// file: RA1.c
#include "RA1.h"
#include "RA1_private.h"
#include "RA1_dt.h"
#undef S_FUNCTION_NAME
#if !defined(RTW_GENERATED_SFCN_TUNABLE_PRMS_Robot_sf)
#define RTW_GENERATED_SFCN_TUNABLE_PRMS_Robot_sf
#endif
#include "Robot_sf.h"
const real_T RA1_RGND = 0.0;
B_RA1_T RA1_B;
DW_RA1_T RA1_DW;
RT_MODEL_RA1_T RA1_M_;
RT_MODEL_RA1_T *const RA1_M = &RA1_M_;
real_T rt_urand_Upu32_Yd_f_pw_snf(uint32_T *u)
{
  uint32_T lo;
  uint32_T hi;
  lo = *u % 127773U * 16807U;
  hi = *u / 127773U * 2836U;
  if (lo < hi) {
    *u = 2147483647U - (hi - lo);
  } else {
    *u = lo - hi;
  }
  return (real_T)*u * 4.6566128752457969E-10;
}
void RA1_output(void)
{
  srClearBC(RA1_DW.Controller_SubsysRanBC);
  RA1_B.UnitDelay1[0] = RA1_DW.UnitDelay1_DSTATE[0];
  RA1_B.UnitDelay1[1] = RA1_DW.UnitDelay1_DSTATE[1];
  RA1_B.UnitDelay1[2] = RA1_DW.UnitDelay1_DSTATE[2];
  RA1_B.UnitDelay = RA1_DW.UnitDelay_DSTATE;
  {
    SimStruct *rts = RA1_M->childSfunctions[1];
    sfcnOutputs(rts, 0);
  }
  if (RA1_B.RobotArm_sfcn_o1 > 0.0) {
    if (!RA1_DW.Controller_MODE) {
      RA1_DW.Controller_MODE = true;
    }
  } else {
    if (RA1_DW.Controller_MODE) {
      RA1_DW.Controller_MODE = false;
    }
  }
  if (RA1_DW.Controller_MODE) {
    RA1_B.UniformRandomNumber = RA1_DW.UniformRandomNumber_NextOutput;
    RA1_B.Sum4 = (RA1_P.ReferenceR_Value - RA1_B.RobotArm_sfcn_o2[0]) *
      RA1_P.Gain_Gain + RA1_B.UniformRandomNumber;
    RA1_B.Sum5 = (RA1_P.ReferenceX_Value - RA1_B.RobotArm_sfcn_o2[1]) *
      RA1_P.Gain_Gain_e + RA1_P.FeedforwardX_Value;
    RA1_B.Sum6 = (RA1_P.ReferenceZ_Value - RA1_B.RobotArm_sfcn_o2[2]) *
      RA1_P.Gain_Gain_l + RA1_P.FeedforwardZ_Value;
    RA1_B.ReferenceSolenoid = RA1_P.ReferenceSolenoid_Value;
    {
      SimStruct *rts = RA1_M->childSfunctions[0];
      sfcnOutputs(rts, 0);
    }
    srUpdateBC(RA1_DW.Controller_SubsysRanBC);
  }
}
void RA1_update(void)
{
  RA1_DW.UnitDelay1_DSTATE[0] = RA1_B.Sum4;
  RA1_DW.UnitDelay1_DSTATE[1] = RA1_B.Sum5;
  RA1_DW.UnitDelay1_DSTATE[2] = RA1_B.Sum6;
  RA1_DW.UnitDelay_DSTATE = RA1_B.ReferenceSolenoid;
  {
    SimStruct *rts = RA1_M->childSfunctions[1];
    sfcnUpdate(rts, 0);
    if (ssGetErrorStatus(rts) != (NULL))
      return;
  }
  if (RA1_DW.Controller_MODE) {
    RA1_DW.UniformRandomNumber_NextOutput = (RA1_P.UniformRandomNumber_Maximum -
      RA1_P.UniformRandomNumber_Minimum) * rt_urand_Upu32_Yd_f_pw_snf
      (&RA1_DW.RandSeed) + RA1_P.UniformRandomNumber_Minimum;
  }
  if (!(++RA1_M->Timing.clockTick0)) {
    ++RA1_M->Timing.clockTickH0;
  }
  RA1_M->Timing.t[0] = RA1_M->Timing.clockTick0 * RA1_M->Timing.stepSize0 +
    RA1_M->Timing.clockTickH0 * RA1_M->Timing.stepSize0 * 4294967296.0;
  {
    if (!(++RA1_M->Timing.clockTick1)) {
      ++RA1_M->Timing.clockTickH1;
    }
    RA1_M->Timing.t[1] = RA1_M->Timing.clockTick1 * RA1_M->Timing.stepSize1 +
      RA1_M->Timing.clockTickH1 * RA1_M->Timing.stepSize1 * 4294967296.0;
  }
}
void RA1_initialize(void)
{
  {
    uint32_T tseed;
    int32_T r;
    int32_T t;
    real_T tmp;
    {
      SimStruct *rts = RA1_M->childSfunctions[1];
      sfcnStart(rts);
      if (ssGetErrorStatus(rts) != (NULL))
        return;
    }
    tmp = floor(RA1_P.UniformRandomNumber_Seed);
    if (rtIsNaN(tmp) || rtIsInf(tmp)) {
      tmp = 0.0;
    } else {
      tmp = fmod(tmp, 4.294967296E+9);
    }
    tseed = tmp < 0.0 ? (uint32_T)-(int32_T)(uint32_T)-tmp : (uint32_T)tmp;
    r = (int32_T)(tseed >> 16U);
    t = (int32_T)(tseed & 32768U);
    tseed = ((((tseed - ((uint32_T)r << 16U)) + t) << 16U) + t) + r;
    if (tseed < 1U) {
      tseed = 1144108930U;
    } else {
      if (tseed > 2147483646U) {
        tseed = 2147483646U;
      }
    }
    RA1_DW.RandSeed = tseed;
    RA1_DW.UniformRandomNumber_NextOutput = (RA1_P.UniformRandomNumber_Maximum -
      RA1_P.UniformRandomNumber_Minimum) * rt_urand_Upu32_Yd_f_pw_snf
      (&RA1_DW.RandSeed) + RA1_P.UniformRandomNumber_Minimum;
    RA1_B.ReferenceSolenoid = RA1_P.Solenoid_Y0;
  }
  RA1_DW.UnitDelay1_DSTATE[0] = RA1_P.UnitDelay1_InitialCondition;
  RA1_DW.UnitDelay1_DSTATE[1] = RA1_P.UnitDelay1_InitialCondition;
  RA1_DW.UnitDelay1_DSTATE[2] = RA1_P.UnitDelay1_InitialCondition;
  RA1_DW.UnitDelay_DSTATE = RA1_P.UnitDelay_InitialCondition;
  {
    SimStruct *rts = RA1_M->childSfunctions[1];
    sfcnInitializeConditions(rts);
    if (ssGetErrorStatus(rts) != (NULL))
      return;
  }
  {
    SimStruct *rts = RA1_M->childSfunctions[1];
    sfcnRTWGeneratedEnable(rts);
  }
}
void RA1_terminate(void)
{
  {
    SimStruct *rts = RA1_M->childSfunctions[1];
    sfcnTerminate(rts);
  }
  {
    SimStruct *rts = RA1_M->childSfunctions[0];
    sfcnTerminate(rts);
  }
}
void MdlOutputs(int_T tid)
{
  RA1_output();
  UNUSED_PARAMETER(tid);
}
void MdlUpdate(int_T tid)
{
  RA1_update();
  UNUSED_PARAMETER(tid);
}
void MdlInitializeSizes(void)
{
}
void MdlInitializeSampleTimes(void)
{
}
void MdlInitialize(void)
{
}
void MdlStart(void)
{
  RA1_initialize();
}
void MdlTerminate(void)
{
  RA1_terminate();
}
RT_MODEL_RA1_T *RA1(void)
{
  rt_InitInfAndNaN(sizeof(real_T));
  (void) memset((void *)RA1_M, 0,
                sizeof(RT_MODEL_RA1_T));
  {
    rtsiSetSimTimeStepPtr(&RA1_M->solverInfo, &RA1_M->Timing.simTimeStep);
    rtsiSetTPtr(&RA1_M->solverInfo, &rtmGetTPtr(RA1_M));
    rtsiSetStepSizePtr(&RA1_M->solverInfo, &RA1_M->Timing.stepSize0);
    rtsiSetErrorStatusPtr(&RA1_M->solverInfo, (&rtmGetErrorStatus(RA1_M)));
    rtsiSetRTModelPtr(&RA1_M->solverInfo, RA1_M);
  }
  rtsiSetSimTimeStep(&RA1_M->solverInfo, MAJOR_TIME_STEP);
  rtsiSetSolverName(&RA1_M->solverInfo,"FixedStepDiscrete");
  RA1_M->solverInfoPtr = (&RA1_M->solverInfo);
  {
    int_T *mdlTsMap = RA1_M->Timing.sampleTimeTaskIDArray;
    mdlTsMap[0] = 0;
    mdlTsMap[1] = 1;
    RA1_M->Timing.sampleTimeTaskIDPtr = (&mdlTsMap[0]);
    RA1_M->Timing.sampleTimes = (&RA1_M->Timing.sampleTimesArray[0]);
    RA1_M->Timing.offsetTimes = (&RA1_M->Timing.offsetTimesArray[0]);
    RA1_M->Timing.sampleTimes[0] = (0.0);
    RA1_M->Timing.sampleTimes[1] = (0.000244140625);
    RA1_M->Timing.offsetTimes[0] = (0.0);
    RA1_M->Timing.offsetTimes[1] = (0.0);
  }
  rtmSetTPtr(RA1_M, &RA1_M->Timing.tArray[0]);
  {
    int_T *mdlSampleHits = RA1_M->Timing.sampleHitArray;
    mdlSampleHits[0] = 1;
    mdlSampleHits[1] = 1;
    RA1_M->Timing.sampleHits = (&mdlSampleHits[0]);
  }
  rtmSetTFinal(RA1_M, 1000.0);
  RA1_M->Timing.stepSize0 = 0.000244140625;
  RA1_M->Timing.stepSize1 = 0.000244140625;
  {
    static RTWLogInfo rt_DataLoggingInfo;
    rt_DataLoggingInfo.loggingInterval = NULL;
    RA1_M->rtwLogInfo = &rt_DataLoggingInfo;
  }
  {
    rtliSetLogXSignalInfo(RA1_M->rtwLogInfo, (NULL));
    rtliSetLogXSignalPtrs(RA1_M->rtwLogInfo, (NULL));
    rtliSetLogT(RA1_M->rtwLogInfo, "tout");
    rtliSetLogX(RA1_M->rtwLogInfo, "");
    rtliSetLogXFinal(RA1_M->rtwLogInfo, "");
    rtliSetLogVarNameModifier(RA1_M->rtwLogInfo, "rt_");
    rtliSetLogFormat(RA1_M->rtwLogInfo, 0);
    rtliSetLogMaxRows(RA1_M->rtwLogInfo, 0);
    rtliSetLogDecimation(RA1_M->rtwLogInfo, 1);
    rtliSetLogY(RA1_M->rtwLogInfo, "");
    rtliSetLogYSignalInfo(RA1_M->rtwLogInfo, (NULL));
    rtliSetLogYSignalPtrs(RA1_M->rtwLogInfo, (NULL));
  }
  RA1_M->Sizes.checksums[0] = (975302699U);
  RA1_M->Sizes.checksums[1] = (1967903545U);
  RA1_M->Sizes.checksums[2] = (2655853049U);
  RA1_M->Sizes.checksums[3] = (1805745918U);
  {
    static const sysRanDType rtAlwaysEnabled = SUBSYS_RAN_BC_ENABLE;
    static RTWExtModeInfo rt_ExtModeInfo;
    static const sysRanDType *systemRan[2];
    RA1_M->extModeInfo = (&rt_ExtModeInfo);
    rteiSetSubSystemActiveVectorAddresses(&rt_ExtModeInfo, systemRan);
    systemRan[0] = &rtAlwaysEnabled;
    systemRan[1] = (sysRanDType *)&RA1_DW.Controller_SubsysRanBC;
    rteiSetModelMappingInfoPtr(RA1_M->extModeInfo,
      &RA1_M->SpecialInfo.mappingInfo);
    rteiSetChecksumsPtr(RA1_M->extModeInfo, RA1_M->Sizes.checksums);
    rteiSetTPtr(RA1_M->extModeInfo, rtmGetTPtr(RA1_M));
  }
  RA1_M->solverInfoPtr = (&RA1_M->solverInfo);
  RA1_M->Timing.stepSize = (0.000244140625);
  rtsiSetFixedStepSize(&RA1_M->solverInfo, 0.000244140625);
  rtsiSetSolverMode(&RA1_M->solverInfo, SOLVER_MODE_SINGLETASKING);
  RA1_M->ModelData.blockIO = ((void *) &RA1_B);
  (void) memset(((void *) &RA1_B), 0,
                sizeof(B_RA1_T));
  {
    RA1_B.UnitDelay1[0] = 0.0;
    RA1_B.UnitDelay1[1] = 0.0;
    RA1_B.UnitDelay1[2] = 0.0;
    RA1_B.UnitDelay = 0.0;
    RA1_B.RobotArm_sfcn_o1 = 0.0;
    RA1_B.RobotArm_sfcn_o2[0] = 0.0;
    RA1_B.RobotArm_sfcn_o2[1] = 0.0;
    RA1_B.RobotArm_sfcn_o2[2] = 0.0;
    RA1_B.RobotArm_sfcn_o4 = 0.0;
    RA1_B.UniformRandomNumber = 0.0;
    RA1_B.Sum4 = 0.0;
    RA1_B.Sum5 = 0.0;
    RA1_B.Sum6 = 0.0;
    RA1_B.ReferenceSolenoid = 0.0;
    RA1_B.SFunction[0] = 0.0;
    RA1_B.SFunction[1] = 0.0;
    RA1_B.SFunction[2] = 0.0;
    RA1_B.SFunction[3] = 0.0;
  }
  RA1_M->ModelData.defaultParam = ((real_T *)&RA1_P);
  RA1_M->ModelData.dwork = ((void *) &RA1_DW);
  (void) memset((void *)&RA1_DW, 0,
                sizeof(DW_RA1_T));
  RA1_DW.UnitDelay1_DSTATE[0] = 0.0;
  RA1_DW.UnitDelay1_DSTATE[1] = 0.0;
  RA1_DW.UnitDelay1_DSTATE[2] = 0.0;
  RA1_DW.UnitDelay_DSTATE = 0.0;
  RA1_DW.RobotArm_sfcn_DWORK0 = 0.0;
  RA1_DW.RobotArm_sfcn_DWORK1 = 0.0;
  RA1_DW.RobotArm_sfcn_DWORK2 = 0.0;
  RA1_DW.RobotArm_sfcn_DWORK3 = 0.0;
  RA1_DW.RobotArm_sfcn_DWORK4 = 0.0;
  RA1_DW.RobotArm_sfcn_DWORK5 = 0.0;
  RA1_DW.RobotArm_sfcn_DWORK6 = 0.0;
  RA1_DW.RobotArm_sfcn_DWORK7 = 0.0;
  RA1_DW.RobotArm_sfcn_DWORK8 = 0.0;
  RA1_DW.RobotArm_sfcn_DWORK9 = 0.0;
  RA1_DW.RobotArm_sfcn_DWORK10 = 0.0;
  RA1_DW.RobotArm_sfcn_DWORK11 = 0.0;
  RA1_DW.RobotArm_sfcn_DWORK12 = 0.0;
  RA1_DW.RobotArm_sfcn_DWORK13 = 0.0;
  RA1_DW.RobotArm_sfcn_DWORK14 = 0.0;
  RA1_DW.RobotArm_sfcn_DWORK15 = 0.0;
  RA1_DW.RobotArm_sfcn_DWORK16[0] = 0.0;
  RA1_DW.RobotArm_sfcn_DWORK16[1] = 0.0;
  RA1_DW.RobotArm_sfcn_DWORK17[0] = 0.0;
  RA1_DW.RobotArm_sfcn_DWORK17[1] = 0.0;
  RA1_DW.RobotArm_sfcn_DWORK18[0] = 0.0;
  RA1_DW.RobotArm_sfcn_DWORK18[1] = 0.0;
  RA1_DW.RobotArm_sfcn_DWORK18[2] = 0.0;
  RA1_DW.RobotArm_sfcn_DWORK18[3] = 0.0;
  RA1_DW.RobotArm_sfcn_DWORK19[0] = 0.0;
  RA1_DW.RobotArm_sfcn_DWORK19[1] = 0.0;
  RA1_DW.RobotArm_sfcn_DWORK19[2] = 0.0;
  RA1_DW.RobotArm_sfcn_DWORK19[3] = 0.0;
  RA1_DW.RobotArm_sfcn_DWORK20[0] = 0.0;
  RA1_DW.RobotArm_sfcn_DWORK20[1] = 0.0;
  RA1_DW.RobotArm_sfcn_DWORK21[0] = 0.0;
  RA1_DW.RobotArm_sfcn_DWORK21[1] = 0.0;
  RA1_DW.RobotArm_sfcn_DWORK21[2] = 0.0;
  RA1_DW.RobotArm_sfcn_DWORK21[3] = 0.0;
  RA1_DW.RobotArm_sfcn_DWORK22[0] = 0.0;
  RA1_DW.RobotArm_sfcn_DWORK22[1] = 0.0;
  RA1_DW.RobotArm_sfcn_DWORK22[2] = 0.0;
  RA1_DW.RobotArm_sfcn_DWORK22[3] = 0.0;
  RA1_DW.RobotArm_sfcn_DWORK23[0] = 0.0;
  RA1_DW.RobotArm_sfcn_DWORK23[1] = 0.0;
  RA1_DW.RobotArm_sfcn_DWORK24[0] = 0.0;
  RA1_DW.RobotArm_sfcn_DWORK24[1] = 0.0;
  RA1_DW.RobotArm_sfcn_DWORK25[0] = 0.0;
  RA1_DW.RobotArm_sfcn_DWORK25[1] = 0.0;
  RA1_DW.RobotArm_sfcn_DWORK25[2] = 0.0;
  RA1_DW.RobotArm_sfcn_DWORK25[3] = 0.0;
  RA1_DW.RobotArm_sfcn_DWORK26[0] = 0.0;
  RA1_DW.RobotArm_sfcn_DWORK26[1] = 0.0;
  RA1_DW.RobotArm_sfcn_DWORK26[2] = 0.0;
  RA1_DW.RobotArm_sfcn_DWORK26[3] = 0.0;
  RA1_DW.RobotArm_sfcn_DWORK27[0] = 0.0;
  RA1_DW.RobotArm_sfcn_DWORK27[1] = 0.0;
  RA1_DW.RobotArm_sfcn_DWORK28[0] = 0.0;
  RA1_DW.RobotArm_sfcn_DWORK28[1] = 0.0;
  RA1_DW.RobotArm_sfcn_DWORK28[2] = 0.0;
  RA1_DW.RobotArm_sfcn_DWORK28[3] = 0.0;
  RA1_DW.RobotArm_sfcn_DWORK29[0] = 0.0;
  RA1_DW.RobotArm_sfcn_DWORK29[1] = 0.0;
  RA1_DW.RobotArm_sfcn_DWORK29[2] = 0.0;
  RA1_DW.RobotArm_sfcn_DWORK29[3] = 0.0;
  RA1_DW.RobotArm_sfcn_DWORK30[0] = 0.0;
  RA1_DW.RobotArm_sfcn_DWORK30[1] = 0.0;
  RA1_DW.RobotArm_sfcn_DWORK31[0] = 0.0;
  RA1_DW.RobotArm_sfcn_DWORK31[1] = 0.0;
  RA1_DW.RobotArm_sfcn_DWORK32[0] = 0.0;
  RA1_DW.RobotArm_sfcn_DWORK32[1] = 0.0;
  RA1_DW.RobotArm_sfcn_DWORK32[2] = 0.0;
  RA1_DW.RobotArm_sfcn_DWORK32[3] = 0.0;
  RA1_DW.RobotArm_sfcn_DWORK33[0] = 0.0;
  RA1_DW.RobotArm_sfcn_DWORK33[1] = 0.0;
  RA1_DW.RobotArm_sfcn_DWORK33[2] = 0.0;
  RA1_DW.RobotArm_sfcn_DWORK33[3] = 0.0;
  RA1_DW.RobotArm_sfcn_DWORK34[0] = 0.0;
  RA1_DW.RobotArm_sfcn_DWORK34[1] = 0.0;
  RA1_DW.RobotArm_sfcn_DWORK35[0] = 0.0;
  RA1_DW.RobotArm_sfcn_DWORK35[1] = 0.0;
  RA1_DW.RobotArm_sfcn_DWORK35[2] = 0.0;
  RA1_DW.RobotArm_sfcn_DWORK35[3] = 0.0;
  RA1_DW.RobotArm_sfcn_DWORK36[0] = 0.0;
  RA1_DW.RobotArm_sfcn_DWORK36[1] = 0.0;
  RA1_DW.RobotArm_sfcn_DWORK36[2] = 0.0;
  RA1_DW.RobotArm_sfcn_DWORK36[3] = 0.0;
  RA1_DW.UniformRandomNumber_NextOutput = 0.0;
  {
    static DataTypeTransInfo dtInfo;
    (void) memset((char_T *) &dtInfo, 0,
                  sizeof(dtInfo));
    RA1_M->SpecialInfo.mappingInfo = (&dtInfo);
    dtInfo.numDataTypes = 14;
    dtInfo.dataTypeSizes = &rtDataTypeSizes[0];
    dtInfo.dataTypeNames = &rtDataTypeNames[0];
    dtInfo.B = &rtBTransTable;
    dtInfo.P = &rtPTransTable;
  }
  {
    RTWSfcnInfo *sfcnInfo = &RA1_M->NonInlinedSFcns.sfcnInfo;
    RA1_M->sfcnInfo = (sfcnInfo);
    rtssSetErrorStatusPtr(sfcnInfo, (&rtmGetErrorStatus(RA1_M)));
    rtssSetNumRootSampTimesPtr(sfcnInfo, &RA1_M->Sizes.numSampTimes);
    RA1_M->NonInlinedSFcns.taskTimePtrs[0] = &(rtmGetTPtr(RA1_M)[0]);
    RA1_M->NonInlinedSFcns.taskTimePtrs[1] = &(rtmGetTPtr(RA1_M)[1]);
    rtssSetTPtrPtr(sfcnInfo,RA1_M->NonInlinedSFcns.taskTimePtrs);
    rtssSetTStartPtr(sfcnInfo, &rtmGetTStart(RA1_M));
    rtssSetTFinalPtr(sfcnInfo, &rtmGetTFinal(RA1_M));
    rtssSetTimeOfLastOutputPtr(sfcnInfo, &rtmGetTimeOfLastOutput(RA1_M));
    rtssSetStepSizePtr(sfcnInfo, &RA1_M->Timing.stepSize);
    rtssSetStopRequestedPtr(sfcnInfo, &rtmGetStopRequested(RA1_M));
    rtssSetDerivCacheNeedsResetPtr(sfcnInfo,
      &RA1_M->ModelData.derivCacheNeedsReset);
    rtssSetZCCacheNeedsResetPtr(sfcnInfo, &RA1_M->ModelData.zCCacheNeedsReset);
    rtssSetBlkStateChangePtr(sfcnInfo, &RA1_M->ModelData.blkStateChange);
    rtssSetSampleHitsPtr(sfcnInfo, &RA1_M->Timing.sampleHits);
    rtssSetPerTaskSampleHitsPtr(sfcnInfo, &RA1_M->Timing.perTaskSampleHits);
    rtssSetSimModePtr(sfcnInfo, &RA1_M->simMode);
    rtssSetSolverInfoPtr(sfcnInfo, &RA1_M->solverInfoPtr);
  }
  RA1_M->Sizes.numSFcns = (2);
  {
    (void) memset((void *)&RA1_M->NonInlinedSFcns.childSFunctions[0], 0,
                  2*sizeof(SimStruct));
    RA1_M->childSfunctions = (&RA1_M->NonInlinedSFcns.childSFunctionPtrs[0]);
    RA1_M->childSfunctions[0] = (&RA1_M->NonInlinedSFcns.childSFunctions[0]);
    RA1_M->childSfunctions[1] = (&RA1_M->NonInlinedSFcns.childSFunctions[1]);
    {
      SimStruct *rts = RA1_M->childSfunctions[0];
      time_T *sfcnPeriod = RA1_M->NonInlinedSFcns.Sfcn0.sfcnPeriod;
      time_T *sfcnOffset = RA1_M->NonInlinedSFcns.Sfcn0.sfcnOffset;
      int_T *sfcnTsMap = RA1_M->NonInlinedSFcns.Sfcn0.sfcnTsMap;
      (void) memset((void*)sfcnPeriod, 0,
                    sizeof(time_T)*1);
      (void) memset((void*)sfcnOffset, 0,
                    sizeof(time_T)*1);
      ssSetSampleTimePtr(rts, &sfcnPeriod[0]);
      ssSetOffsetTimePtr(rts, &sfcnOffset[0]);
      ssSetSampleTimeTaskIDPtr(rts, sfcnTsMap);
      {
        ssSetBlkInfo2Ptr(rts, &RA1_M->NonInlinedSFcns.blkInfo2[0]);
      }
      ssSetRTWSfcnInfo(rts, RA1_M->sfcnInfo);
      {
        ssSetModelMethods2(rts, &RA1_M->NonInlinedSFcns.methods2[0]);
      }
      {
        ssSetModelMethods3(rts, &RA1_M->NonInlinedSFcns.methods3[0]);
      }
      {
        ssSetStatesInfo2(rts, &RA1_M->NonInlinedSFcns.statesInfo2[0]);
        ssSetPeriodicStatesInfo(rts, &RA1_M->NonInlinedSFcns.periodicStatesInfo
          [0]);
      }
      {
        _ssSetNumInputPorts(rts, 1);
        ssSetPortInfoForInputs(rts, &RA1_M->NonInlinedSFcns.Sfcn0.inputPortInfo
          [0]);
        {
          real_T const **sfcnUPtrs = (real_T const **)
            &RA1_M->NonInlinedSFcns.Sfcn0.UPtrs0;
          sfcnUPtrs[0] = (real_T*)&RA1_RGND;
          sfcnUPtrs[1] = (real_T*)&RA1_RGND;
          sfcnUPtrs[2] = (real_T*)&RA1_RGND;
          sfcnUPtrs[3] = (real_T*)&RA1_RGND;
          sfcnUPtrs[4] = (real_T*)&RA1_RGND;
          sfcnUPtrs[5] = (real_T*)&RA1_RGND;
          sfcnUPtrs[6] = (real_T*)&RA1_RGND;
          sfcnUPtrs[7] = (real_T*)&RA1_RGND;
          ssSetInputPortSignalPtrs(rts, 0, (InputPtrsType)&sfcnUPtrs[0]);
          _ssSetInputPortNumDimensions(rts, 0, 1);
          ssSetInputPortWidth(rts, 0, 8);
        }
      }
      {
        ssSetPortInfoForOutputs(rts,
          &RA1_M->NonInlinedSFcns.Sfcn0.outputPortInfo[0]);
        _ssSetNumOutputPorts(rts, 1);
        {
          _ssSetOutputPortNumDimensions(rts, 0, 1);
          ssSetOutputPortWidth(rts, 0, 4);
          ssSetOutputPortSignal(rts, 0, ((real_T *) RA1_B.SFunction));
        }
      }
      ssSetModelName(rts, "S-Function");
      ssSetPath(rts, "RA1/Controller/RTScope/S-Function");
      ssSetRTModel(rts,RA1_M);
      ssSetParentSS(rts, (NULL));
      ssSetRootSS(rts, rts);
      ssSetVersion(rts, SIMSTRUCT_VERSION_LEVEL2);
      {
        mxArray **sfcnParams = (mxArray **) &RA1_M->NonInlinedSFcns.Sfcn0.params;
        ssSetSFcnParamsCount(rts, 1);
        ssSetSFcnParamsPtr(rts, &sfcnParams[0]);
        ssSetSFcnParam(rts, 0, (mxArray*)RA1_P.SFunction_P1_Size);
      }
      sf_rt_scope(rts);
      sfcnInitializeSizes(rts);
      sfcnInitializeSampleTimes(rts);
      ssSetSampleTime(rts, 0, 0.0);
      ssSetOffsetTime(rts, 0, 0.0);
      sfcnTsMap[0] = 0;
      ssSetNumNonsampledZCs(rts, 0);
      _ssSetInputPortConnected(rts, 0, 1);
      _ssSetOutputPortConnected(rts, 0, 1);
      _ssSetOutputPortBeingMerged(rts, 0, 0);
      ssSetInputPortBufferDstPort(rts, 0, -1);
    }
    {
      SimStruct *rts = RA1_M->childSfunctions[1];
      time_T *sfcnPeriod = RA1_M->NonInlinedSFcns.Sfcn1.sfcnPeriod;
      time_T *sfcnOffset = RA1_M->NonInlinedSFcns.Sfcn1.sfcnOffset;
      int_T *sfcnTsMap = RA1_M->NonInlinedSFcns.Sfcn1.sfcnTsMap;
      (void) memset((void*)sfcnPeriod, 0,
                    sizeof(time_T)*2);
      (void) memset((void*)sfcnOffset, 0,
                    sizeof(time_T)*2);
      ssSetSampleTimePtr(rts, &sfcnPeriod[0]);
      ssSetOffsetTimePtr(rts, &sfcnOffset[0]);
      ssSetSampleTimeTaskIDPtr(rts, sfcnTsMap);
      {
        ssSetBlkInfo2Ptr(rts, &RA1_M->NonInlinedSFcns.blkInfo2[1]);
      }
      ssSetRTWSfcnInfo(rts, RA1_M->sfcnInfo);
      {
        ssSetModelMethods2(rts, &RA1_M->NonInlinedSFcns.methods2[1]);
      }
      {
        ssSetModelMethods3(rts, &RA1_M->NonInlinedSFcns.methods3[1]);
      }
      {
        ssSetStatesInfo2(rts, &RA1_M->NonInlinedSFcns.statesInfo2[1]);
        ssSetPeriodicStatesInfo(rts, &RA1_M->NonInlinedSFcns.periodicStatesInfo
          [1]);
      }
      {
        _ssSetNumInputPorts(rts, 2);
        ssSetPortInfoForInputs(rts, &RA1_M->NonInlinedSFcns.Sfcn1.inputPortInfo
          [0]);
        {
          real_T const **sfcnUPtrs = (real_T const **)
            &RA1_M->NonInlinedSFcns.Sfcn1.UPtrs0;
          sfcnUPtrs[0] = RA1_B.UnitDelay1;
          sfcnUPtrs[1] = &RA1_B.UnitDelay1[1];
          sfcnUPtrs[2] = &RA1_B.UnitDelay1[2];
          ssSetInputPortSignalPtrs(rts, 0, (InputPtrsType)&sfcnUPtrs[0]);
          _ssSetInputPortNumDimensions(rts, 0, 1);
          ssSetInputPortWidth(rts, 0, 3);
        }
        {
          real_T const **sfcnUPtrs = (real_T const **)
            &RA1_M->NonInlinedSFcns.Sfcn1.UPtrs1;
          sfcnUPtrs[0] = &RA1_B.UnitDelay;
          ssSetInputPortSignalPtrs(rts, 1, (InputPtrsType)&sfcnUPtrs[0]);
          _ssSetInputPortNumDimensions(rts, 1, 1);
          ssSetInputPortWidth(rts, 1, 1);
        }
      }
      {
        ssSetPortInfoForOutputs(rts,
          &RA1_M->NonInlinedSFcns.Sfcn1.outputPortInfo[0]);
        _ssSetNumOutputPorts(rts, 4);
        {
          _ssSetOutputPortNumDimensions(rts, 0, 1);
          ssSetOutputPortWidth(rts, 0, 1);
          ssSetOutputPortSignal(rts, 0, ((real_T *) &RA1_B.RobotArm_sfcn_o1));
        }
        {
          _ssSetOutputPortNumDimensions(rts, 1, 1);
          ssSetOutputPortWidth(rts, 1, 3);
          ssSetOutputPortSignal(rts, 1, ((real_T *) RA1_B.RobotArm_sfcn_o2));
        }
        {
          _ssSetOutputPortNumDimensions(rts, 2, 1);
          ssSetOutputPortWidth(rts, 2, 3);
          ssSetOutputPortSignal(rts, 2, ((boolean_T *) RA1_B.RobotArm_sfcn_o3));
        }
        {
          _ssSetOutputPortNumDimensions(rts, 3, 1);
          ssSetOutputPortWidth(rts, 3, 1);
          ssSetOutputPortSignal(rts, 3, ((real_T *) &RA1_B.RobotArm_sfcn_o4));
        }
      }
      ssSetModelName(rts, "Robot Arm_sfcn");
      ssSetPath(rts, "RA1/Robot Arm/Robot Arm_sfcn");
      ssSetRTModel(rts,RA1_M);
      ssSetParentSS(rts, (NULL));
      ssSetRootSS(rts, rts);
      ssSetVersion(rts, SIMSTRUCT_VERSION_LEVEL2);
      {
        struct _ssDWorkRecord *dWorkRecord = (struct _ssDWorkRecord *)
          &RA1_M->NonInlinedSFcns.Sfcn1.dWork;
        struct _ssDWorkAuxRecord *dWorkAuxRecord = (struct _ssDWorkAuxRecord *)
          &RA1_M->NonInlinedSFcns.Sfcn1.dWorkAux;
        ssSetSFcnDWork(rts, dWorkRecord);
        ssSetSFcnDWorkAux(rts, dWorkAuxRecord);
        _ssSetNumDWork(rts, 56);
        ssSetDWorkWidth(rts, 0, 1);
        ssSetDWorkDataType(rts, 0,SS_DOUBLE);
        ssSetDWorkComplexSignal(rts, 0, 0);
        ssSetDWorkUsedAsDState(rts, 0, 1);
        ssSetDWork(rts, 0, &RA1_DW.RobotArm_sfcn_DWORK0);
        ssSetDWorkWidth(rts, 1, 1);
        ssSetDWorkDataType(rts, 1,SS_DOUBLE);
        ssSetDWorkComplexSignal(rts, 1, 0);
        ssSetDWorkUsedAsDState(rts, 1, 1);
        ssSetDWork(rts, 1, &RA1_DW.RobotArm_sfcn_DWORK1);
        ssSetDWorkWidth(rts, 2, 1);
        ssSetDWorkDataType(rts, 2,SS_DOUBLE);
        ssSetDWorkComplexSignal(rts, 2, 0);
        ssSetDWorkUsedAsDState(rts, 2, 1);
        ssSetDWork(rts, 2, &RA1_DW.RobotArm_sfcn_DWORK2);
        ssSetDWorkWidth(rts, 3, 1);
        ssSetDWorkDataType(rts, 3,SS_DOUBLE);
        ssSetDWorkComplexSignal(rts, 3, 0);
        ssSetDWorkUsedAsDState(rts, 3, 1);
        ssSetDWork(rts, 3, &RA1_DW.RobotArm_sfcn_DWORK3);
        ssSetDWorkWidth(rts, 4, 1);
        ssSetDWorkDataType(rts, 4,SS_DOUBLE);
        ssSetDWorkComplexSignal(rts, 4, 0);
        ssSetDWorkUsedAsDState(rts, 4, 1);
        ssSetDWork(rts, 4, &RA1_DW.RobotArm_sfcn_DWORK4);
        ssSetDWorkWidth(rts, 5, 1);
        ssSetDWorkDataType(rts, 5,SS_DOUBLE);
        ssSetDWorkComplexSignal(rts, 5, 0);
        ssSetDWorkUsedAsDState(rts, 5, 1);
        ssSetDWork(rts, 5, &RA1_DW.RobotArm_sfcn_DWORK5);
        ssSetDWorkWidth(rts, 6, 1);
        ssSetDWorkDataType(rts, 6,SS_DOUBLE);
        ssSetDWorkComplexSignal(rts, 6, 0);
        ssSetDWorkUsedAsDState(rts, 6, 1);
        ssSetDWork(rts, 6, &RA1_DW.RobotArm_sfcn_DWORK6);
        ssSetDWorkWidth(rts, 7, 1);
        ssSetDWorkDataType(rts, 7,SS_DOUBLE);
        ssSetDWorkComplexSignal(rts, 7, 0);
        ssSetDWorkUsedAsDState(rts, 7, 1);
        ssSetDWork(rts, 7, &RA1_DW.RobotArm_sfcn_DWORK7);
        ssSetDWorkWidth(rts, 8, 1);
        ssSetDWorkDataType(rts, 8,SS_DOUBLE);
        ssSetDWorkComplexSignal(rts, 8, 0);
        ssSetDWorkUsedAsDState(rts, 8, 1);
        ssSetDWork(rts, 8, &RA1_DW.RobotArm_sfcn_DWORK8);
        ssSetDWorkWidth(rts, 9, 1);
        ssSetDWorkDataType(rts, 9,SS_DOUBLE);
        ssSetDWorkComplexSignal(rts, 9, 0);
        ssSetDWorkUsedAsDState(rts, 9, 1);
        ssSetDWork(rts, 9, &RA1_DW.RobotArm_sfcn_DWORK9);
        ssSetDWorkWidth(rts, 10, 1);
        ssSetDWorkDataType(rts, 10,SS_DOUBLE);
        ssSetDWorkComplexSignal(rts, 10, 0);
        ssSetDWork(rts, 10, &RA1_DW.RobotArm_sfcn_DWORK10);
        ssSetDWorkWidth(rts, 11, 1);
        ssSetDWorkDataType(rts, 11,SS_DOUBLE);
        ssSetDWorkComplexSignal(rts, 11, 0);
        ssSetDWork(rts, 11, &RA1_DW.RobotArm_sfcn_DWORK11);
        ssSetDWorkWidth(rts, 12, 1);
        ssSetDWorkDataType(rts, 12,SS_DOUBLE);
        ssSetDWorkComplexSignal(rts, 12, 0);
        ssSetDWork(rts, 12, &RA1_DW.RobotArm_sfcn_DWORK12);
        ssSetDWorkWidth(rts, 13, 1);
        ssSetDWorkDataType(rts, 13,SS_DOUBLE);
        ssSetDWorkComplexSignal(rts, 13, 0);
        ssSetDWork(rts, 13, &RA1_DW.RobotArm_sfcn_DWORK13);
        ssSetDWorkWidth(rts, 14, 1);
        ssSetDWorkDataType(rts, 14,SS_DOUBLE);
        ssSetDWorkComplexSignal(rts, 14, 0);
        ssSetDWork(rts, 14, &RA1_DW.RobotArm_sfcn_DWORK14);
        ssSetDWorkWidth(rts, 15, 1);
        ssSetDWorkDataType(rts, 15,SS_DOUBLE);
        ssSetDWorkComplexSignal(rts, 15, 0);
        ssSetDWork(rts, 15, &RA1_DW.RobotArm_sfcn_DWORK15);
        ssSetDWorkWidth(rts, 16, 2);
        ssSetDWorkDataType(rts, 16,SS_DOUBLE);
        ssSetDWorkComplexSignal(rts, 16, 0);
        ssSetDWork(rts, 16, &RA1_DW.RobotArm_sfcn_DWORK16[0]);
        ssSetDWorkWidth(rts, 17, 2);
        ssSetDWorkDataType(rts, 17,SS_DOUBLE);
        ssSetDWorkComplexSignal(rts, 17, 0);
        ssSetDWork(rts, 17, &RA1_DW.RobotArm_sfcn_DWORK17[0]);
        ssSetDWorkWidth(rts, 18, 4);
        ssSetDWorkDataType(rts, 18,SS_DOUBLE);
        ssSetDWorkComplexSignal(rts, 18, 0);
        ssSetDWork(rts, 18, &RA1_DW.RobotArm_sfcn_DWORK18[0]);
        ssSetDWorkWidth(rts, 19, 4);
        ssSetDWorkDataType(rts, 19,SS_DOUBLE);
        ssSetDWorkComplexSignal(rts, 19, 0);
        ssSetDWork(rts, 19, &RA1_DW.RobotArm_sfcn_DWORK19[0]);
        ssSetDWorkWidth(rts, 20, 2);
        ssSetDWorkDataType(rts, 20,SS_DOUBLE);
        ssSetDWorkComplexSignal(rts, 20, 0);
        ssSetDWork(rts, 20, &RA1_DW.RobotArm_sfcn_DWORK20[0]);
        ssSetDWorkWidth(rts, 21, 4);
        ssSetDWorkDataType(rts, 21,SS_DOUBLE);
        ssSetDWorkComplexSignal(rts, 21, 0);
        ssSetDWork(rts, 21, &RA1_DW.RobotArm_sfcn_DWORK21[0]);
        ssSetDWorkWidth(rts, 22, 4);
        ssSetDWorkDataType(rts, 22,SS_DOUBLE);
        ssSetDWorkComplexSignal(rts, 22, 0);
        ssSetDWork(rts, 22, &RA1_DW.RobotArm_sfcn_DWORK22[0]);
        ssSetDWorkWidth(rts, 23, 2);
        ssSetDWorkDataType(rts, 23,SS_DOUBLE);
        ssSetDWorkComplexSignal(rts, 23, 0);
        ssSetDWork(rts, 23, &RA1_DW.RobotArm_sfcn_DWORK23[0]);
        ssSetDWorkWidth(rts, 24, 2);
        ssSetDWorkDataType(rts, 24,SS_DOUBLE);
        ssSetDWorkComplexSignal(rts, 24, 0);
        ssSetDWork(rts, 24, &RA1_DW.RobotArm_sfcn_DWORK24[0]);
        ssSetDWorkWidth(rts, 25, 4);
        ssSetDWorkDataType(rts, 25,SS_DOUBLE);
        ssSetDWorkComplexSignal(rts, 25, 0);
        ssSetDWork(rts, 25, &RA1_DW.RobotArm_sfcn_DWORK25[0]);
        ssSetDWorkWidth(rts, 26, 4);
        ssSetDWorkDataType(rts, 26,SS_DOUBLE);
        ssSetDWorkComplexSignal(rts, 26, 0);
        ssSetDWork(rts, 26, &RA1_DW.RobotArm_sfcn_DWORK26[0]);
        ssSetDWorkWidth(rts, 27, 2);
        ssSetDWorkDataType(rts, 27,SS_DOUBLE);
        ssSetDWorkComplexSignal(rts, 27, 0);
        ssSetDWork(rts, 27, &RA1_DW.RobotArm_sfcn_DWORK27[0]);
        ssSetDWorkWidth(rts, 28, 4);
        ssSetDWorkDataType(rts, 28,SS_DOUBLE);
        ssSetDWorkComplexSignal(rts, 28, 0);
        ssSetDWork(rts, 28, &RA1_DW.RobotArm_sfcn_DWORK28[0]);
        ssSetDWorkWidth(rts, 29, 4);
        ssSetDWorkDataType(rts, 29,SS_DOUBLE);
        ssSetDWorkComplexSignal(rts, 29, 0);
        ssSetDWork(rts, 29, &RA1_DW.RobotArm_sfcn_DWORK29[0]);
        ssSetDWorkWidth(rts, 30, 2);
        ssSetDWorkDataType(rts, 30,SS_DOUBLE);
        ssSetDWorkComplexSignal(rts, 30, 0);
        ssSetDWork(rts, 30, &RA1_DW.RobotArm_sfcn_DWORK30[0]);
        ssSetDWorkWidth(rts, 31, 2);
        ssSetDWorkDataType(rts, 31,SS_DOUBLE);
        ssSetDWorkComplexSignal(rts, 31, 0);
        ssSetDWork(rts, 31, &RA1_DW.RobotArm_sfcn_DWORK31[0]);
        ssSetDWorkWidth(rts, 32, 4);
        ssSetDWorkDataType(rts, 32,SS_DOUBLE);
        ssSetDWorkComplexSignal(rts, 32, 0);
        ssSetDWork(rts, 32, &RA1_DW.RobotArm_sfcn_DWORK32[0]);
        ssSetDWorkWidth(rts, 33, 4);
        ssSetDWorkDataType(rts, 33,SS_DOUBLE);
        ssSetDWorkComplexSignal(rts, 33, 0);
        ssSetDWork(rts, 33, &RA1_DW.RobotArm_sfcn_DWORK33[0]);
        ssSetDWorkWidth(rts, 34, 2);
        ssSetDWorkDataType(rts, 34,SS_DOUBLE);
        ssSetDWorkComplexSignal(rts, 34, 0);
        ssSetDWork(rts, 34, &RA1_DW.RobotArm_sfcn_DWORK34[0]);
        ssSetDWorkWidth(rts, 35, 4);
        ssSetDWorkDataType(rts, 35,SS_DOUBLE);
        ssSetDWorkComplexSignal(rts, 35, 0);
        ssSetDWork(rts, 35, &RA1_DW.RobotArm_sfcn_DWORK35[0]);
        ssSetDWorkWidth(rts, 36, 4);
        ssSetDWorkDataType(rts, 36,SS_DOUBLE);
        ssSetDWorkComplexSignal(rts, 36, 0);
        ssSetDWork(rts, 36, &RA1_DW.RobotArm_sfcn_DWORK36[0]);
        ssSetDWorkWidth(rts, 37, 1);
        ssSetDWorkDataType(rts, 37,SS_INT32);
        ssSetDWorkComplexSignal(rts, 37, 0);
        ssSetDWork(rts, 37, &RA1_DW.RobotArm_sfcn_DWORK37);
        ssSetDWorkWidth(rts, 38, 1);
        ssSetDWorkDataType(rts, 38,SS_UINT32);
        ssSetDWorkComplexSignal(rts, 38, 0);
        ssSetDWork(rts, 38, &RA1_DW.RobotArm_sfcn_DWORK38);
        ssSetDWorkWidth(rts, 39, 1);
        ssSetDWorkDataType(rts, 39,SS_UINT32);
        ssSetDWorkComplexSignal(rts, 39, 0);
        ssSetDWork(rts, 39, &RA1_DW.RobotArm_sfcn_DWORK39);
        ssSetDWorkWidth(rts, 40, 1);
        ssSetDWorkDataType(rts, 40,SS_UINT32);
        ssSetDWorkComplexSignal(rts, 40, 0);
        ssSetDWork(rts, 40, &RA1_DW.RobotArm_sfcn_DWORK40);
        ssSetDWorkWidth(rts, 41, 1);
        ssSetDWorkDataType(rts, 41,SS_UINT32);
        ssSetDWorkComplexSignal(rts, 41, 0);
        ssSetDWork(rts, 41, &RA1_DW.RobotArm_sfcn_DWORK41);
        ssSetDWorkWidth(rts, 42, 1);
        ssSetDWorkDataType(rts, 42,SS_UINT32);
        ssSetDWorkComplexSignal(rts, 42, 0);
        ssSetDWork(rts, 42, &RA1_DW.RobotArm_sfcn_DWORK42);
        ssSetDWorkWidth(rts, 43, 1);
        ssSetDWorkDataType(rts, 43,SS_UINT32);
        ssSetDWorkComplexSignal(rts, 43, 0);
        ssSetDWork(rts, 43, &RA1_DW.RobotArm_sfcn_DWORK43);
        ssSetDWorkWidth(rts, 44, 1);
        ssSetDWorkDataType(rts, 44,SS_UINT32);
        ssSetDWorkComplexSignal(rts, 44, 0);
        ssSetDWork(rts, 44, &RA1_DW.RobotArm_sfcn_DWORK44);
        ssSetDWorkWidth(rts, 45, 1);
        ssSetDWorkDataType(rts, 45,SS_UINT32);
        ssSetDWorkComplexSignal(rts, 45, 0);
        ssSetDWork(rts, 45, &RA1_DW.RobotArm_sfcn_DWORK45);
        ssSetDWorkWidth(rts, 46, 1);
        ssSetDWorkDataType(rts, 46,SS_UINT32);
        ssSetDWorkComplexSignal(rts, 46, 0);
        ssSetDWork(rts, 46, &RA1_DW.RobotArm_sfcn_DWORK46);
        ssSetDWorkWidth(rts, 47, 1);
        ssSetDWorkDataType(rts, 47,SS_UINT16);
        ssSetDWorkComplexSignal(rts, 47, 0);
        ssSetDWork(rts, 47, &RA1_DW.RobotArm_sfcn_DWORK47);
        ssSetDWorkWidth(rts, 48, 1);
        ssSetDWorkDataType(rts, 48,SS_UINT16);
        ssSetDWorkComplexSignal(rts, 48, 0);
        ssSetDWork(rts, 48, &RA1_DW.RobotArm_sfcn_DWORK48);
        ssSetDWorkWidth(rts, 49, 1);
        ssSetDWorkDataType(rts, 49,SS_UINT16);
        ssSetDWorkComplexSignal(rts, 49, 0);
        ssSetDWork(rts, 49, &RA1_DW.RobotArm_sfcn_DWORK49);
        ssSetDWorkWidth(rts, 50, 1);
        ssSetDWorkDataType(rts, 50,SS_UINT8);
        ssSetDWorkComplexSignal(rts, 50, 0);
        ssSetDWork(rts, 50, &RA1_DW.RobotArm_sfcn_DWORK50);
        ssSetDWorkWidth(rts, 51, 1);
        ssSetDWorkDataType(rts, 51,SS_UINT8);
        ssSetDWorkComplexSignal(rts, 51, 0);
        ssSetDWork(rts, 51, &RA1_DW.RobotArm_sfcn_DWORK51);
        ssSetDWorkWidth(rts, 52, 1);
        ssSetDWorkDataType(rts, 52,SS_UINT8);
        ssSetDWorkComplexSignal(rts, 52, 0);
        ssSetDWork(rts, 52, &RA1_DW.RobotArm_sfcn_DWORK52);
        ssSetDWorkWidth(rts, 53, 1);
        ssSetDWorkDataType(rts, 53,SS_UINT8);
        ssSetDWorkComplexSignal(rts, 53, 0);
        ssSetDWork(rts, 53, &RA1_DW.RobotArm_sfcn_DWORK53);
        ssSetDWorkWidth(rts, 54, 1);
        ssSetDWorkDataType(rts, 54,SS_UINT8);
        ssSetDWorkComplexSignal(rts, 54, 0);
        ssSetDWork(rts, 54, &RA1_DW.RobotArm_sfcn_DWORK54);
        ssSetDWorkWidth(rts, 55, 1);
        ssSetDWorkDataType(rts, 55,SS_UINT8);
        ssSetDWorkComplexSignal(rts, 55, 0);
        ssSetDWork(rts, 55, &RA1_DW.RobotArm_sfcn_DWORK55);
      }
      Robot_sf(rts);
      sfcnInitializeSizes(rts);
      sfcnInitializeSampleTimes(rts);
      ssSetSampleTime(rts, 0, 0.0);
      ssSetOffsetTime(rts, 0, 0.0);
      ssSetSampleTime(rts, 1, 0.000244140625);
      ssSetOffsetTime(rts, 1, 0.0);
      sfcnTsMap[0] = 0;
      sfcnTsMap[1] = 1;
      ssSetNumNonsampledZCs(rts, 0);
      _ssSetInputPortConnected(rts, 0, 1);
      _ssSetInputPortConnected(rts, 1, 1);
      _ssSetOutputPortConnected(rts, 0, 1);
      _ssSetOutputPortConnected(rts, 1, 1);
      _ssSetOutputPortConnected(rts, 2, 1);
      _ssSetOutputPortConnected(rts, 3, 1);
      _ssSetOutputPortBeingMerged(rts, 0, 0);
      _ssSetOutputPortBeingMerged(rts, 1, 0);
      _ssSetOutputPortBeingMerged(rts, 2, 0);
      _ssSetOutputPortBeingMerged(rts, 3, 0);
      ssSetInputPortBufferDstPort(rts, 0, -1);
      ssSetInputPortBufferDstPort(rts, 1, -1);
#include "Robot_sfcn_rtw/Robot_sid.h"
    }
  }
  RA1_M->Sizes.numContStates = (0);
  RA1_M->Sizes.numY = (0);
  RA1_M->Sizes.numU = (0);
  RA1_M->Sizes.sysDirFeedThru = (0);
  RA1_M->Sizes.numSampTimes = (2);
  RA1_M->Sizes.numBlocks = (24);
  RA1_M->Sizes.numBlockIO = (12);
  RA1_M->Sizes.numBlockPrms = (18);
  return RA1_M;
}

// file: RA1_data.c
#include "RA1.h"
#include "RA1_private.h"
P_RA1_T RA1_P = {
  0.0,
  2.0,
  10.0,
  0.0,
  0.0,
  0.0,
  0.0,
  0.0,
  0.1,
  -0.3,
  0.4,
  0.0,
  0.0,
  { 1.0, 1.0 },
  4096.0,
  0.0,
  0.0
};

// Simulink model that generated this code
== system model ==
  UnitDelay1 : UnitDelay  <- 1: Controller
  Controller : Subsystem  <- 1: RobotArm_sfcn/2, Enable: RobotArm_sfcn
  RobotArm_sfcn : S-Function  FunctionName=Robot_sf  <- 1: UnitDelay1, 2: UnitDelay
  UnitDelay : UnitDelay  <- 1: Controller/2
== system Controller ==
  Inport#1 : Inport
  EnablePort#1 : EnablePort
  Outport#1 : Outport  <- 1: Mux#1
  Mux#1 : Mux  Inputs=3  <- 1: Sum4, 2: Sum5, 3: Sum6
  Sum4 : Sum  Inputs=++  <- 1: UniformRandomNumber, 2: Gain
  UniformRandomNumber : UniformRandomNumber
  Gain : Gain  Gain=10  <- 1: Sum#1
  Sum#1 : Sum  Inputs=+-  <- 1: ReferenceR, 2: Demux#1
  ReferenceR : Constant  Value=2
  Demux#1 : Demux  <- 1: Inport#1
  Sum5 : Sum  Inputs=++  <- 1: FeedforwardX, 2: Gain#1
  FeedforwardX : Constant  Value=0
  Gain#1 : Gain  Gain=0  <- 1: Sum#2
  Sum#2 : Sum  Inputs=+-  <- 1: ReferenceX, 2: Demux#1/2
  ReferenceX : Constant  Value=0
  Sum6 : Sum  Inputs=++  <- 1: FeedforwardZ, 2: Gain#2
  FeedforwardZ : Constant  Value=0.1
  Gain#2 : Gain  Gain=0  <- 1: Sum#3
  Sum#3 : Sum  Inputs=+-  <- 1: ReferenceZ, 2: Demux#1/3
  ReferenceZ : Constant  Value=0
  Solenoid : Outport  InitialOutput=0  <- 1: ReferenceSolenoid
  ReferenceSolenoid : Constant  Value=0
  SFunction : S-Function  FunctionName=sf_rt_scope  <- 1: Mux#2
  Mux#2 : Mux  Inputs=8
